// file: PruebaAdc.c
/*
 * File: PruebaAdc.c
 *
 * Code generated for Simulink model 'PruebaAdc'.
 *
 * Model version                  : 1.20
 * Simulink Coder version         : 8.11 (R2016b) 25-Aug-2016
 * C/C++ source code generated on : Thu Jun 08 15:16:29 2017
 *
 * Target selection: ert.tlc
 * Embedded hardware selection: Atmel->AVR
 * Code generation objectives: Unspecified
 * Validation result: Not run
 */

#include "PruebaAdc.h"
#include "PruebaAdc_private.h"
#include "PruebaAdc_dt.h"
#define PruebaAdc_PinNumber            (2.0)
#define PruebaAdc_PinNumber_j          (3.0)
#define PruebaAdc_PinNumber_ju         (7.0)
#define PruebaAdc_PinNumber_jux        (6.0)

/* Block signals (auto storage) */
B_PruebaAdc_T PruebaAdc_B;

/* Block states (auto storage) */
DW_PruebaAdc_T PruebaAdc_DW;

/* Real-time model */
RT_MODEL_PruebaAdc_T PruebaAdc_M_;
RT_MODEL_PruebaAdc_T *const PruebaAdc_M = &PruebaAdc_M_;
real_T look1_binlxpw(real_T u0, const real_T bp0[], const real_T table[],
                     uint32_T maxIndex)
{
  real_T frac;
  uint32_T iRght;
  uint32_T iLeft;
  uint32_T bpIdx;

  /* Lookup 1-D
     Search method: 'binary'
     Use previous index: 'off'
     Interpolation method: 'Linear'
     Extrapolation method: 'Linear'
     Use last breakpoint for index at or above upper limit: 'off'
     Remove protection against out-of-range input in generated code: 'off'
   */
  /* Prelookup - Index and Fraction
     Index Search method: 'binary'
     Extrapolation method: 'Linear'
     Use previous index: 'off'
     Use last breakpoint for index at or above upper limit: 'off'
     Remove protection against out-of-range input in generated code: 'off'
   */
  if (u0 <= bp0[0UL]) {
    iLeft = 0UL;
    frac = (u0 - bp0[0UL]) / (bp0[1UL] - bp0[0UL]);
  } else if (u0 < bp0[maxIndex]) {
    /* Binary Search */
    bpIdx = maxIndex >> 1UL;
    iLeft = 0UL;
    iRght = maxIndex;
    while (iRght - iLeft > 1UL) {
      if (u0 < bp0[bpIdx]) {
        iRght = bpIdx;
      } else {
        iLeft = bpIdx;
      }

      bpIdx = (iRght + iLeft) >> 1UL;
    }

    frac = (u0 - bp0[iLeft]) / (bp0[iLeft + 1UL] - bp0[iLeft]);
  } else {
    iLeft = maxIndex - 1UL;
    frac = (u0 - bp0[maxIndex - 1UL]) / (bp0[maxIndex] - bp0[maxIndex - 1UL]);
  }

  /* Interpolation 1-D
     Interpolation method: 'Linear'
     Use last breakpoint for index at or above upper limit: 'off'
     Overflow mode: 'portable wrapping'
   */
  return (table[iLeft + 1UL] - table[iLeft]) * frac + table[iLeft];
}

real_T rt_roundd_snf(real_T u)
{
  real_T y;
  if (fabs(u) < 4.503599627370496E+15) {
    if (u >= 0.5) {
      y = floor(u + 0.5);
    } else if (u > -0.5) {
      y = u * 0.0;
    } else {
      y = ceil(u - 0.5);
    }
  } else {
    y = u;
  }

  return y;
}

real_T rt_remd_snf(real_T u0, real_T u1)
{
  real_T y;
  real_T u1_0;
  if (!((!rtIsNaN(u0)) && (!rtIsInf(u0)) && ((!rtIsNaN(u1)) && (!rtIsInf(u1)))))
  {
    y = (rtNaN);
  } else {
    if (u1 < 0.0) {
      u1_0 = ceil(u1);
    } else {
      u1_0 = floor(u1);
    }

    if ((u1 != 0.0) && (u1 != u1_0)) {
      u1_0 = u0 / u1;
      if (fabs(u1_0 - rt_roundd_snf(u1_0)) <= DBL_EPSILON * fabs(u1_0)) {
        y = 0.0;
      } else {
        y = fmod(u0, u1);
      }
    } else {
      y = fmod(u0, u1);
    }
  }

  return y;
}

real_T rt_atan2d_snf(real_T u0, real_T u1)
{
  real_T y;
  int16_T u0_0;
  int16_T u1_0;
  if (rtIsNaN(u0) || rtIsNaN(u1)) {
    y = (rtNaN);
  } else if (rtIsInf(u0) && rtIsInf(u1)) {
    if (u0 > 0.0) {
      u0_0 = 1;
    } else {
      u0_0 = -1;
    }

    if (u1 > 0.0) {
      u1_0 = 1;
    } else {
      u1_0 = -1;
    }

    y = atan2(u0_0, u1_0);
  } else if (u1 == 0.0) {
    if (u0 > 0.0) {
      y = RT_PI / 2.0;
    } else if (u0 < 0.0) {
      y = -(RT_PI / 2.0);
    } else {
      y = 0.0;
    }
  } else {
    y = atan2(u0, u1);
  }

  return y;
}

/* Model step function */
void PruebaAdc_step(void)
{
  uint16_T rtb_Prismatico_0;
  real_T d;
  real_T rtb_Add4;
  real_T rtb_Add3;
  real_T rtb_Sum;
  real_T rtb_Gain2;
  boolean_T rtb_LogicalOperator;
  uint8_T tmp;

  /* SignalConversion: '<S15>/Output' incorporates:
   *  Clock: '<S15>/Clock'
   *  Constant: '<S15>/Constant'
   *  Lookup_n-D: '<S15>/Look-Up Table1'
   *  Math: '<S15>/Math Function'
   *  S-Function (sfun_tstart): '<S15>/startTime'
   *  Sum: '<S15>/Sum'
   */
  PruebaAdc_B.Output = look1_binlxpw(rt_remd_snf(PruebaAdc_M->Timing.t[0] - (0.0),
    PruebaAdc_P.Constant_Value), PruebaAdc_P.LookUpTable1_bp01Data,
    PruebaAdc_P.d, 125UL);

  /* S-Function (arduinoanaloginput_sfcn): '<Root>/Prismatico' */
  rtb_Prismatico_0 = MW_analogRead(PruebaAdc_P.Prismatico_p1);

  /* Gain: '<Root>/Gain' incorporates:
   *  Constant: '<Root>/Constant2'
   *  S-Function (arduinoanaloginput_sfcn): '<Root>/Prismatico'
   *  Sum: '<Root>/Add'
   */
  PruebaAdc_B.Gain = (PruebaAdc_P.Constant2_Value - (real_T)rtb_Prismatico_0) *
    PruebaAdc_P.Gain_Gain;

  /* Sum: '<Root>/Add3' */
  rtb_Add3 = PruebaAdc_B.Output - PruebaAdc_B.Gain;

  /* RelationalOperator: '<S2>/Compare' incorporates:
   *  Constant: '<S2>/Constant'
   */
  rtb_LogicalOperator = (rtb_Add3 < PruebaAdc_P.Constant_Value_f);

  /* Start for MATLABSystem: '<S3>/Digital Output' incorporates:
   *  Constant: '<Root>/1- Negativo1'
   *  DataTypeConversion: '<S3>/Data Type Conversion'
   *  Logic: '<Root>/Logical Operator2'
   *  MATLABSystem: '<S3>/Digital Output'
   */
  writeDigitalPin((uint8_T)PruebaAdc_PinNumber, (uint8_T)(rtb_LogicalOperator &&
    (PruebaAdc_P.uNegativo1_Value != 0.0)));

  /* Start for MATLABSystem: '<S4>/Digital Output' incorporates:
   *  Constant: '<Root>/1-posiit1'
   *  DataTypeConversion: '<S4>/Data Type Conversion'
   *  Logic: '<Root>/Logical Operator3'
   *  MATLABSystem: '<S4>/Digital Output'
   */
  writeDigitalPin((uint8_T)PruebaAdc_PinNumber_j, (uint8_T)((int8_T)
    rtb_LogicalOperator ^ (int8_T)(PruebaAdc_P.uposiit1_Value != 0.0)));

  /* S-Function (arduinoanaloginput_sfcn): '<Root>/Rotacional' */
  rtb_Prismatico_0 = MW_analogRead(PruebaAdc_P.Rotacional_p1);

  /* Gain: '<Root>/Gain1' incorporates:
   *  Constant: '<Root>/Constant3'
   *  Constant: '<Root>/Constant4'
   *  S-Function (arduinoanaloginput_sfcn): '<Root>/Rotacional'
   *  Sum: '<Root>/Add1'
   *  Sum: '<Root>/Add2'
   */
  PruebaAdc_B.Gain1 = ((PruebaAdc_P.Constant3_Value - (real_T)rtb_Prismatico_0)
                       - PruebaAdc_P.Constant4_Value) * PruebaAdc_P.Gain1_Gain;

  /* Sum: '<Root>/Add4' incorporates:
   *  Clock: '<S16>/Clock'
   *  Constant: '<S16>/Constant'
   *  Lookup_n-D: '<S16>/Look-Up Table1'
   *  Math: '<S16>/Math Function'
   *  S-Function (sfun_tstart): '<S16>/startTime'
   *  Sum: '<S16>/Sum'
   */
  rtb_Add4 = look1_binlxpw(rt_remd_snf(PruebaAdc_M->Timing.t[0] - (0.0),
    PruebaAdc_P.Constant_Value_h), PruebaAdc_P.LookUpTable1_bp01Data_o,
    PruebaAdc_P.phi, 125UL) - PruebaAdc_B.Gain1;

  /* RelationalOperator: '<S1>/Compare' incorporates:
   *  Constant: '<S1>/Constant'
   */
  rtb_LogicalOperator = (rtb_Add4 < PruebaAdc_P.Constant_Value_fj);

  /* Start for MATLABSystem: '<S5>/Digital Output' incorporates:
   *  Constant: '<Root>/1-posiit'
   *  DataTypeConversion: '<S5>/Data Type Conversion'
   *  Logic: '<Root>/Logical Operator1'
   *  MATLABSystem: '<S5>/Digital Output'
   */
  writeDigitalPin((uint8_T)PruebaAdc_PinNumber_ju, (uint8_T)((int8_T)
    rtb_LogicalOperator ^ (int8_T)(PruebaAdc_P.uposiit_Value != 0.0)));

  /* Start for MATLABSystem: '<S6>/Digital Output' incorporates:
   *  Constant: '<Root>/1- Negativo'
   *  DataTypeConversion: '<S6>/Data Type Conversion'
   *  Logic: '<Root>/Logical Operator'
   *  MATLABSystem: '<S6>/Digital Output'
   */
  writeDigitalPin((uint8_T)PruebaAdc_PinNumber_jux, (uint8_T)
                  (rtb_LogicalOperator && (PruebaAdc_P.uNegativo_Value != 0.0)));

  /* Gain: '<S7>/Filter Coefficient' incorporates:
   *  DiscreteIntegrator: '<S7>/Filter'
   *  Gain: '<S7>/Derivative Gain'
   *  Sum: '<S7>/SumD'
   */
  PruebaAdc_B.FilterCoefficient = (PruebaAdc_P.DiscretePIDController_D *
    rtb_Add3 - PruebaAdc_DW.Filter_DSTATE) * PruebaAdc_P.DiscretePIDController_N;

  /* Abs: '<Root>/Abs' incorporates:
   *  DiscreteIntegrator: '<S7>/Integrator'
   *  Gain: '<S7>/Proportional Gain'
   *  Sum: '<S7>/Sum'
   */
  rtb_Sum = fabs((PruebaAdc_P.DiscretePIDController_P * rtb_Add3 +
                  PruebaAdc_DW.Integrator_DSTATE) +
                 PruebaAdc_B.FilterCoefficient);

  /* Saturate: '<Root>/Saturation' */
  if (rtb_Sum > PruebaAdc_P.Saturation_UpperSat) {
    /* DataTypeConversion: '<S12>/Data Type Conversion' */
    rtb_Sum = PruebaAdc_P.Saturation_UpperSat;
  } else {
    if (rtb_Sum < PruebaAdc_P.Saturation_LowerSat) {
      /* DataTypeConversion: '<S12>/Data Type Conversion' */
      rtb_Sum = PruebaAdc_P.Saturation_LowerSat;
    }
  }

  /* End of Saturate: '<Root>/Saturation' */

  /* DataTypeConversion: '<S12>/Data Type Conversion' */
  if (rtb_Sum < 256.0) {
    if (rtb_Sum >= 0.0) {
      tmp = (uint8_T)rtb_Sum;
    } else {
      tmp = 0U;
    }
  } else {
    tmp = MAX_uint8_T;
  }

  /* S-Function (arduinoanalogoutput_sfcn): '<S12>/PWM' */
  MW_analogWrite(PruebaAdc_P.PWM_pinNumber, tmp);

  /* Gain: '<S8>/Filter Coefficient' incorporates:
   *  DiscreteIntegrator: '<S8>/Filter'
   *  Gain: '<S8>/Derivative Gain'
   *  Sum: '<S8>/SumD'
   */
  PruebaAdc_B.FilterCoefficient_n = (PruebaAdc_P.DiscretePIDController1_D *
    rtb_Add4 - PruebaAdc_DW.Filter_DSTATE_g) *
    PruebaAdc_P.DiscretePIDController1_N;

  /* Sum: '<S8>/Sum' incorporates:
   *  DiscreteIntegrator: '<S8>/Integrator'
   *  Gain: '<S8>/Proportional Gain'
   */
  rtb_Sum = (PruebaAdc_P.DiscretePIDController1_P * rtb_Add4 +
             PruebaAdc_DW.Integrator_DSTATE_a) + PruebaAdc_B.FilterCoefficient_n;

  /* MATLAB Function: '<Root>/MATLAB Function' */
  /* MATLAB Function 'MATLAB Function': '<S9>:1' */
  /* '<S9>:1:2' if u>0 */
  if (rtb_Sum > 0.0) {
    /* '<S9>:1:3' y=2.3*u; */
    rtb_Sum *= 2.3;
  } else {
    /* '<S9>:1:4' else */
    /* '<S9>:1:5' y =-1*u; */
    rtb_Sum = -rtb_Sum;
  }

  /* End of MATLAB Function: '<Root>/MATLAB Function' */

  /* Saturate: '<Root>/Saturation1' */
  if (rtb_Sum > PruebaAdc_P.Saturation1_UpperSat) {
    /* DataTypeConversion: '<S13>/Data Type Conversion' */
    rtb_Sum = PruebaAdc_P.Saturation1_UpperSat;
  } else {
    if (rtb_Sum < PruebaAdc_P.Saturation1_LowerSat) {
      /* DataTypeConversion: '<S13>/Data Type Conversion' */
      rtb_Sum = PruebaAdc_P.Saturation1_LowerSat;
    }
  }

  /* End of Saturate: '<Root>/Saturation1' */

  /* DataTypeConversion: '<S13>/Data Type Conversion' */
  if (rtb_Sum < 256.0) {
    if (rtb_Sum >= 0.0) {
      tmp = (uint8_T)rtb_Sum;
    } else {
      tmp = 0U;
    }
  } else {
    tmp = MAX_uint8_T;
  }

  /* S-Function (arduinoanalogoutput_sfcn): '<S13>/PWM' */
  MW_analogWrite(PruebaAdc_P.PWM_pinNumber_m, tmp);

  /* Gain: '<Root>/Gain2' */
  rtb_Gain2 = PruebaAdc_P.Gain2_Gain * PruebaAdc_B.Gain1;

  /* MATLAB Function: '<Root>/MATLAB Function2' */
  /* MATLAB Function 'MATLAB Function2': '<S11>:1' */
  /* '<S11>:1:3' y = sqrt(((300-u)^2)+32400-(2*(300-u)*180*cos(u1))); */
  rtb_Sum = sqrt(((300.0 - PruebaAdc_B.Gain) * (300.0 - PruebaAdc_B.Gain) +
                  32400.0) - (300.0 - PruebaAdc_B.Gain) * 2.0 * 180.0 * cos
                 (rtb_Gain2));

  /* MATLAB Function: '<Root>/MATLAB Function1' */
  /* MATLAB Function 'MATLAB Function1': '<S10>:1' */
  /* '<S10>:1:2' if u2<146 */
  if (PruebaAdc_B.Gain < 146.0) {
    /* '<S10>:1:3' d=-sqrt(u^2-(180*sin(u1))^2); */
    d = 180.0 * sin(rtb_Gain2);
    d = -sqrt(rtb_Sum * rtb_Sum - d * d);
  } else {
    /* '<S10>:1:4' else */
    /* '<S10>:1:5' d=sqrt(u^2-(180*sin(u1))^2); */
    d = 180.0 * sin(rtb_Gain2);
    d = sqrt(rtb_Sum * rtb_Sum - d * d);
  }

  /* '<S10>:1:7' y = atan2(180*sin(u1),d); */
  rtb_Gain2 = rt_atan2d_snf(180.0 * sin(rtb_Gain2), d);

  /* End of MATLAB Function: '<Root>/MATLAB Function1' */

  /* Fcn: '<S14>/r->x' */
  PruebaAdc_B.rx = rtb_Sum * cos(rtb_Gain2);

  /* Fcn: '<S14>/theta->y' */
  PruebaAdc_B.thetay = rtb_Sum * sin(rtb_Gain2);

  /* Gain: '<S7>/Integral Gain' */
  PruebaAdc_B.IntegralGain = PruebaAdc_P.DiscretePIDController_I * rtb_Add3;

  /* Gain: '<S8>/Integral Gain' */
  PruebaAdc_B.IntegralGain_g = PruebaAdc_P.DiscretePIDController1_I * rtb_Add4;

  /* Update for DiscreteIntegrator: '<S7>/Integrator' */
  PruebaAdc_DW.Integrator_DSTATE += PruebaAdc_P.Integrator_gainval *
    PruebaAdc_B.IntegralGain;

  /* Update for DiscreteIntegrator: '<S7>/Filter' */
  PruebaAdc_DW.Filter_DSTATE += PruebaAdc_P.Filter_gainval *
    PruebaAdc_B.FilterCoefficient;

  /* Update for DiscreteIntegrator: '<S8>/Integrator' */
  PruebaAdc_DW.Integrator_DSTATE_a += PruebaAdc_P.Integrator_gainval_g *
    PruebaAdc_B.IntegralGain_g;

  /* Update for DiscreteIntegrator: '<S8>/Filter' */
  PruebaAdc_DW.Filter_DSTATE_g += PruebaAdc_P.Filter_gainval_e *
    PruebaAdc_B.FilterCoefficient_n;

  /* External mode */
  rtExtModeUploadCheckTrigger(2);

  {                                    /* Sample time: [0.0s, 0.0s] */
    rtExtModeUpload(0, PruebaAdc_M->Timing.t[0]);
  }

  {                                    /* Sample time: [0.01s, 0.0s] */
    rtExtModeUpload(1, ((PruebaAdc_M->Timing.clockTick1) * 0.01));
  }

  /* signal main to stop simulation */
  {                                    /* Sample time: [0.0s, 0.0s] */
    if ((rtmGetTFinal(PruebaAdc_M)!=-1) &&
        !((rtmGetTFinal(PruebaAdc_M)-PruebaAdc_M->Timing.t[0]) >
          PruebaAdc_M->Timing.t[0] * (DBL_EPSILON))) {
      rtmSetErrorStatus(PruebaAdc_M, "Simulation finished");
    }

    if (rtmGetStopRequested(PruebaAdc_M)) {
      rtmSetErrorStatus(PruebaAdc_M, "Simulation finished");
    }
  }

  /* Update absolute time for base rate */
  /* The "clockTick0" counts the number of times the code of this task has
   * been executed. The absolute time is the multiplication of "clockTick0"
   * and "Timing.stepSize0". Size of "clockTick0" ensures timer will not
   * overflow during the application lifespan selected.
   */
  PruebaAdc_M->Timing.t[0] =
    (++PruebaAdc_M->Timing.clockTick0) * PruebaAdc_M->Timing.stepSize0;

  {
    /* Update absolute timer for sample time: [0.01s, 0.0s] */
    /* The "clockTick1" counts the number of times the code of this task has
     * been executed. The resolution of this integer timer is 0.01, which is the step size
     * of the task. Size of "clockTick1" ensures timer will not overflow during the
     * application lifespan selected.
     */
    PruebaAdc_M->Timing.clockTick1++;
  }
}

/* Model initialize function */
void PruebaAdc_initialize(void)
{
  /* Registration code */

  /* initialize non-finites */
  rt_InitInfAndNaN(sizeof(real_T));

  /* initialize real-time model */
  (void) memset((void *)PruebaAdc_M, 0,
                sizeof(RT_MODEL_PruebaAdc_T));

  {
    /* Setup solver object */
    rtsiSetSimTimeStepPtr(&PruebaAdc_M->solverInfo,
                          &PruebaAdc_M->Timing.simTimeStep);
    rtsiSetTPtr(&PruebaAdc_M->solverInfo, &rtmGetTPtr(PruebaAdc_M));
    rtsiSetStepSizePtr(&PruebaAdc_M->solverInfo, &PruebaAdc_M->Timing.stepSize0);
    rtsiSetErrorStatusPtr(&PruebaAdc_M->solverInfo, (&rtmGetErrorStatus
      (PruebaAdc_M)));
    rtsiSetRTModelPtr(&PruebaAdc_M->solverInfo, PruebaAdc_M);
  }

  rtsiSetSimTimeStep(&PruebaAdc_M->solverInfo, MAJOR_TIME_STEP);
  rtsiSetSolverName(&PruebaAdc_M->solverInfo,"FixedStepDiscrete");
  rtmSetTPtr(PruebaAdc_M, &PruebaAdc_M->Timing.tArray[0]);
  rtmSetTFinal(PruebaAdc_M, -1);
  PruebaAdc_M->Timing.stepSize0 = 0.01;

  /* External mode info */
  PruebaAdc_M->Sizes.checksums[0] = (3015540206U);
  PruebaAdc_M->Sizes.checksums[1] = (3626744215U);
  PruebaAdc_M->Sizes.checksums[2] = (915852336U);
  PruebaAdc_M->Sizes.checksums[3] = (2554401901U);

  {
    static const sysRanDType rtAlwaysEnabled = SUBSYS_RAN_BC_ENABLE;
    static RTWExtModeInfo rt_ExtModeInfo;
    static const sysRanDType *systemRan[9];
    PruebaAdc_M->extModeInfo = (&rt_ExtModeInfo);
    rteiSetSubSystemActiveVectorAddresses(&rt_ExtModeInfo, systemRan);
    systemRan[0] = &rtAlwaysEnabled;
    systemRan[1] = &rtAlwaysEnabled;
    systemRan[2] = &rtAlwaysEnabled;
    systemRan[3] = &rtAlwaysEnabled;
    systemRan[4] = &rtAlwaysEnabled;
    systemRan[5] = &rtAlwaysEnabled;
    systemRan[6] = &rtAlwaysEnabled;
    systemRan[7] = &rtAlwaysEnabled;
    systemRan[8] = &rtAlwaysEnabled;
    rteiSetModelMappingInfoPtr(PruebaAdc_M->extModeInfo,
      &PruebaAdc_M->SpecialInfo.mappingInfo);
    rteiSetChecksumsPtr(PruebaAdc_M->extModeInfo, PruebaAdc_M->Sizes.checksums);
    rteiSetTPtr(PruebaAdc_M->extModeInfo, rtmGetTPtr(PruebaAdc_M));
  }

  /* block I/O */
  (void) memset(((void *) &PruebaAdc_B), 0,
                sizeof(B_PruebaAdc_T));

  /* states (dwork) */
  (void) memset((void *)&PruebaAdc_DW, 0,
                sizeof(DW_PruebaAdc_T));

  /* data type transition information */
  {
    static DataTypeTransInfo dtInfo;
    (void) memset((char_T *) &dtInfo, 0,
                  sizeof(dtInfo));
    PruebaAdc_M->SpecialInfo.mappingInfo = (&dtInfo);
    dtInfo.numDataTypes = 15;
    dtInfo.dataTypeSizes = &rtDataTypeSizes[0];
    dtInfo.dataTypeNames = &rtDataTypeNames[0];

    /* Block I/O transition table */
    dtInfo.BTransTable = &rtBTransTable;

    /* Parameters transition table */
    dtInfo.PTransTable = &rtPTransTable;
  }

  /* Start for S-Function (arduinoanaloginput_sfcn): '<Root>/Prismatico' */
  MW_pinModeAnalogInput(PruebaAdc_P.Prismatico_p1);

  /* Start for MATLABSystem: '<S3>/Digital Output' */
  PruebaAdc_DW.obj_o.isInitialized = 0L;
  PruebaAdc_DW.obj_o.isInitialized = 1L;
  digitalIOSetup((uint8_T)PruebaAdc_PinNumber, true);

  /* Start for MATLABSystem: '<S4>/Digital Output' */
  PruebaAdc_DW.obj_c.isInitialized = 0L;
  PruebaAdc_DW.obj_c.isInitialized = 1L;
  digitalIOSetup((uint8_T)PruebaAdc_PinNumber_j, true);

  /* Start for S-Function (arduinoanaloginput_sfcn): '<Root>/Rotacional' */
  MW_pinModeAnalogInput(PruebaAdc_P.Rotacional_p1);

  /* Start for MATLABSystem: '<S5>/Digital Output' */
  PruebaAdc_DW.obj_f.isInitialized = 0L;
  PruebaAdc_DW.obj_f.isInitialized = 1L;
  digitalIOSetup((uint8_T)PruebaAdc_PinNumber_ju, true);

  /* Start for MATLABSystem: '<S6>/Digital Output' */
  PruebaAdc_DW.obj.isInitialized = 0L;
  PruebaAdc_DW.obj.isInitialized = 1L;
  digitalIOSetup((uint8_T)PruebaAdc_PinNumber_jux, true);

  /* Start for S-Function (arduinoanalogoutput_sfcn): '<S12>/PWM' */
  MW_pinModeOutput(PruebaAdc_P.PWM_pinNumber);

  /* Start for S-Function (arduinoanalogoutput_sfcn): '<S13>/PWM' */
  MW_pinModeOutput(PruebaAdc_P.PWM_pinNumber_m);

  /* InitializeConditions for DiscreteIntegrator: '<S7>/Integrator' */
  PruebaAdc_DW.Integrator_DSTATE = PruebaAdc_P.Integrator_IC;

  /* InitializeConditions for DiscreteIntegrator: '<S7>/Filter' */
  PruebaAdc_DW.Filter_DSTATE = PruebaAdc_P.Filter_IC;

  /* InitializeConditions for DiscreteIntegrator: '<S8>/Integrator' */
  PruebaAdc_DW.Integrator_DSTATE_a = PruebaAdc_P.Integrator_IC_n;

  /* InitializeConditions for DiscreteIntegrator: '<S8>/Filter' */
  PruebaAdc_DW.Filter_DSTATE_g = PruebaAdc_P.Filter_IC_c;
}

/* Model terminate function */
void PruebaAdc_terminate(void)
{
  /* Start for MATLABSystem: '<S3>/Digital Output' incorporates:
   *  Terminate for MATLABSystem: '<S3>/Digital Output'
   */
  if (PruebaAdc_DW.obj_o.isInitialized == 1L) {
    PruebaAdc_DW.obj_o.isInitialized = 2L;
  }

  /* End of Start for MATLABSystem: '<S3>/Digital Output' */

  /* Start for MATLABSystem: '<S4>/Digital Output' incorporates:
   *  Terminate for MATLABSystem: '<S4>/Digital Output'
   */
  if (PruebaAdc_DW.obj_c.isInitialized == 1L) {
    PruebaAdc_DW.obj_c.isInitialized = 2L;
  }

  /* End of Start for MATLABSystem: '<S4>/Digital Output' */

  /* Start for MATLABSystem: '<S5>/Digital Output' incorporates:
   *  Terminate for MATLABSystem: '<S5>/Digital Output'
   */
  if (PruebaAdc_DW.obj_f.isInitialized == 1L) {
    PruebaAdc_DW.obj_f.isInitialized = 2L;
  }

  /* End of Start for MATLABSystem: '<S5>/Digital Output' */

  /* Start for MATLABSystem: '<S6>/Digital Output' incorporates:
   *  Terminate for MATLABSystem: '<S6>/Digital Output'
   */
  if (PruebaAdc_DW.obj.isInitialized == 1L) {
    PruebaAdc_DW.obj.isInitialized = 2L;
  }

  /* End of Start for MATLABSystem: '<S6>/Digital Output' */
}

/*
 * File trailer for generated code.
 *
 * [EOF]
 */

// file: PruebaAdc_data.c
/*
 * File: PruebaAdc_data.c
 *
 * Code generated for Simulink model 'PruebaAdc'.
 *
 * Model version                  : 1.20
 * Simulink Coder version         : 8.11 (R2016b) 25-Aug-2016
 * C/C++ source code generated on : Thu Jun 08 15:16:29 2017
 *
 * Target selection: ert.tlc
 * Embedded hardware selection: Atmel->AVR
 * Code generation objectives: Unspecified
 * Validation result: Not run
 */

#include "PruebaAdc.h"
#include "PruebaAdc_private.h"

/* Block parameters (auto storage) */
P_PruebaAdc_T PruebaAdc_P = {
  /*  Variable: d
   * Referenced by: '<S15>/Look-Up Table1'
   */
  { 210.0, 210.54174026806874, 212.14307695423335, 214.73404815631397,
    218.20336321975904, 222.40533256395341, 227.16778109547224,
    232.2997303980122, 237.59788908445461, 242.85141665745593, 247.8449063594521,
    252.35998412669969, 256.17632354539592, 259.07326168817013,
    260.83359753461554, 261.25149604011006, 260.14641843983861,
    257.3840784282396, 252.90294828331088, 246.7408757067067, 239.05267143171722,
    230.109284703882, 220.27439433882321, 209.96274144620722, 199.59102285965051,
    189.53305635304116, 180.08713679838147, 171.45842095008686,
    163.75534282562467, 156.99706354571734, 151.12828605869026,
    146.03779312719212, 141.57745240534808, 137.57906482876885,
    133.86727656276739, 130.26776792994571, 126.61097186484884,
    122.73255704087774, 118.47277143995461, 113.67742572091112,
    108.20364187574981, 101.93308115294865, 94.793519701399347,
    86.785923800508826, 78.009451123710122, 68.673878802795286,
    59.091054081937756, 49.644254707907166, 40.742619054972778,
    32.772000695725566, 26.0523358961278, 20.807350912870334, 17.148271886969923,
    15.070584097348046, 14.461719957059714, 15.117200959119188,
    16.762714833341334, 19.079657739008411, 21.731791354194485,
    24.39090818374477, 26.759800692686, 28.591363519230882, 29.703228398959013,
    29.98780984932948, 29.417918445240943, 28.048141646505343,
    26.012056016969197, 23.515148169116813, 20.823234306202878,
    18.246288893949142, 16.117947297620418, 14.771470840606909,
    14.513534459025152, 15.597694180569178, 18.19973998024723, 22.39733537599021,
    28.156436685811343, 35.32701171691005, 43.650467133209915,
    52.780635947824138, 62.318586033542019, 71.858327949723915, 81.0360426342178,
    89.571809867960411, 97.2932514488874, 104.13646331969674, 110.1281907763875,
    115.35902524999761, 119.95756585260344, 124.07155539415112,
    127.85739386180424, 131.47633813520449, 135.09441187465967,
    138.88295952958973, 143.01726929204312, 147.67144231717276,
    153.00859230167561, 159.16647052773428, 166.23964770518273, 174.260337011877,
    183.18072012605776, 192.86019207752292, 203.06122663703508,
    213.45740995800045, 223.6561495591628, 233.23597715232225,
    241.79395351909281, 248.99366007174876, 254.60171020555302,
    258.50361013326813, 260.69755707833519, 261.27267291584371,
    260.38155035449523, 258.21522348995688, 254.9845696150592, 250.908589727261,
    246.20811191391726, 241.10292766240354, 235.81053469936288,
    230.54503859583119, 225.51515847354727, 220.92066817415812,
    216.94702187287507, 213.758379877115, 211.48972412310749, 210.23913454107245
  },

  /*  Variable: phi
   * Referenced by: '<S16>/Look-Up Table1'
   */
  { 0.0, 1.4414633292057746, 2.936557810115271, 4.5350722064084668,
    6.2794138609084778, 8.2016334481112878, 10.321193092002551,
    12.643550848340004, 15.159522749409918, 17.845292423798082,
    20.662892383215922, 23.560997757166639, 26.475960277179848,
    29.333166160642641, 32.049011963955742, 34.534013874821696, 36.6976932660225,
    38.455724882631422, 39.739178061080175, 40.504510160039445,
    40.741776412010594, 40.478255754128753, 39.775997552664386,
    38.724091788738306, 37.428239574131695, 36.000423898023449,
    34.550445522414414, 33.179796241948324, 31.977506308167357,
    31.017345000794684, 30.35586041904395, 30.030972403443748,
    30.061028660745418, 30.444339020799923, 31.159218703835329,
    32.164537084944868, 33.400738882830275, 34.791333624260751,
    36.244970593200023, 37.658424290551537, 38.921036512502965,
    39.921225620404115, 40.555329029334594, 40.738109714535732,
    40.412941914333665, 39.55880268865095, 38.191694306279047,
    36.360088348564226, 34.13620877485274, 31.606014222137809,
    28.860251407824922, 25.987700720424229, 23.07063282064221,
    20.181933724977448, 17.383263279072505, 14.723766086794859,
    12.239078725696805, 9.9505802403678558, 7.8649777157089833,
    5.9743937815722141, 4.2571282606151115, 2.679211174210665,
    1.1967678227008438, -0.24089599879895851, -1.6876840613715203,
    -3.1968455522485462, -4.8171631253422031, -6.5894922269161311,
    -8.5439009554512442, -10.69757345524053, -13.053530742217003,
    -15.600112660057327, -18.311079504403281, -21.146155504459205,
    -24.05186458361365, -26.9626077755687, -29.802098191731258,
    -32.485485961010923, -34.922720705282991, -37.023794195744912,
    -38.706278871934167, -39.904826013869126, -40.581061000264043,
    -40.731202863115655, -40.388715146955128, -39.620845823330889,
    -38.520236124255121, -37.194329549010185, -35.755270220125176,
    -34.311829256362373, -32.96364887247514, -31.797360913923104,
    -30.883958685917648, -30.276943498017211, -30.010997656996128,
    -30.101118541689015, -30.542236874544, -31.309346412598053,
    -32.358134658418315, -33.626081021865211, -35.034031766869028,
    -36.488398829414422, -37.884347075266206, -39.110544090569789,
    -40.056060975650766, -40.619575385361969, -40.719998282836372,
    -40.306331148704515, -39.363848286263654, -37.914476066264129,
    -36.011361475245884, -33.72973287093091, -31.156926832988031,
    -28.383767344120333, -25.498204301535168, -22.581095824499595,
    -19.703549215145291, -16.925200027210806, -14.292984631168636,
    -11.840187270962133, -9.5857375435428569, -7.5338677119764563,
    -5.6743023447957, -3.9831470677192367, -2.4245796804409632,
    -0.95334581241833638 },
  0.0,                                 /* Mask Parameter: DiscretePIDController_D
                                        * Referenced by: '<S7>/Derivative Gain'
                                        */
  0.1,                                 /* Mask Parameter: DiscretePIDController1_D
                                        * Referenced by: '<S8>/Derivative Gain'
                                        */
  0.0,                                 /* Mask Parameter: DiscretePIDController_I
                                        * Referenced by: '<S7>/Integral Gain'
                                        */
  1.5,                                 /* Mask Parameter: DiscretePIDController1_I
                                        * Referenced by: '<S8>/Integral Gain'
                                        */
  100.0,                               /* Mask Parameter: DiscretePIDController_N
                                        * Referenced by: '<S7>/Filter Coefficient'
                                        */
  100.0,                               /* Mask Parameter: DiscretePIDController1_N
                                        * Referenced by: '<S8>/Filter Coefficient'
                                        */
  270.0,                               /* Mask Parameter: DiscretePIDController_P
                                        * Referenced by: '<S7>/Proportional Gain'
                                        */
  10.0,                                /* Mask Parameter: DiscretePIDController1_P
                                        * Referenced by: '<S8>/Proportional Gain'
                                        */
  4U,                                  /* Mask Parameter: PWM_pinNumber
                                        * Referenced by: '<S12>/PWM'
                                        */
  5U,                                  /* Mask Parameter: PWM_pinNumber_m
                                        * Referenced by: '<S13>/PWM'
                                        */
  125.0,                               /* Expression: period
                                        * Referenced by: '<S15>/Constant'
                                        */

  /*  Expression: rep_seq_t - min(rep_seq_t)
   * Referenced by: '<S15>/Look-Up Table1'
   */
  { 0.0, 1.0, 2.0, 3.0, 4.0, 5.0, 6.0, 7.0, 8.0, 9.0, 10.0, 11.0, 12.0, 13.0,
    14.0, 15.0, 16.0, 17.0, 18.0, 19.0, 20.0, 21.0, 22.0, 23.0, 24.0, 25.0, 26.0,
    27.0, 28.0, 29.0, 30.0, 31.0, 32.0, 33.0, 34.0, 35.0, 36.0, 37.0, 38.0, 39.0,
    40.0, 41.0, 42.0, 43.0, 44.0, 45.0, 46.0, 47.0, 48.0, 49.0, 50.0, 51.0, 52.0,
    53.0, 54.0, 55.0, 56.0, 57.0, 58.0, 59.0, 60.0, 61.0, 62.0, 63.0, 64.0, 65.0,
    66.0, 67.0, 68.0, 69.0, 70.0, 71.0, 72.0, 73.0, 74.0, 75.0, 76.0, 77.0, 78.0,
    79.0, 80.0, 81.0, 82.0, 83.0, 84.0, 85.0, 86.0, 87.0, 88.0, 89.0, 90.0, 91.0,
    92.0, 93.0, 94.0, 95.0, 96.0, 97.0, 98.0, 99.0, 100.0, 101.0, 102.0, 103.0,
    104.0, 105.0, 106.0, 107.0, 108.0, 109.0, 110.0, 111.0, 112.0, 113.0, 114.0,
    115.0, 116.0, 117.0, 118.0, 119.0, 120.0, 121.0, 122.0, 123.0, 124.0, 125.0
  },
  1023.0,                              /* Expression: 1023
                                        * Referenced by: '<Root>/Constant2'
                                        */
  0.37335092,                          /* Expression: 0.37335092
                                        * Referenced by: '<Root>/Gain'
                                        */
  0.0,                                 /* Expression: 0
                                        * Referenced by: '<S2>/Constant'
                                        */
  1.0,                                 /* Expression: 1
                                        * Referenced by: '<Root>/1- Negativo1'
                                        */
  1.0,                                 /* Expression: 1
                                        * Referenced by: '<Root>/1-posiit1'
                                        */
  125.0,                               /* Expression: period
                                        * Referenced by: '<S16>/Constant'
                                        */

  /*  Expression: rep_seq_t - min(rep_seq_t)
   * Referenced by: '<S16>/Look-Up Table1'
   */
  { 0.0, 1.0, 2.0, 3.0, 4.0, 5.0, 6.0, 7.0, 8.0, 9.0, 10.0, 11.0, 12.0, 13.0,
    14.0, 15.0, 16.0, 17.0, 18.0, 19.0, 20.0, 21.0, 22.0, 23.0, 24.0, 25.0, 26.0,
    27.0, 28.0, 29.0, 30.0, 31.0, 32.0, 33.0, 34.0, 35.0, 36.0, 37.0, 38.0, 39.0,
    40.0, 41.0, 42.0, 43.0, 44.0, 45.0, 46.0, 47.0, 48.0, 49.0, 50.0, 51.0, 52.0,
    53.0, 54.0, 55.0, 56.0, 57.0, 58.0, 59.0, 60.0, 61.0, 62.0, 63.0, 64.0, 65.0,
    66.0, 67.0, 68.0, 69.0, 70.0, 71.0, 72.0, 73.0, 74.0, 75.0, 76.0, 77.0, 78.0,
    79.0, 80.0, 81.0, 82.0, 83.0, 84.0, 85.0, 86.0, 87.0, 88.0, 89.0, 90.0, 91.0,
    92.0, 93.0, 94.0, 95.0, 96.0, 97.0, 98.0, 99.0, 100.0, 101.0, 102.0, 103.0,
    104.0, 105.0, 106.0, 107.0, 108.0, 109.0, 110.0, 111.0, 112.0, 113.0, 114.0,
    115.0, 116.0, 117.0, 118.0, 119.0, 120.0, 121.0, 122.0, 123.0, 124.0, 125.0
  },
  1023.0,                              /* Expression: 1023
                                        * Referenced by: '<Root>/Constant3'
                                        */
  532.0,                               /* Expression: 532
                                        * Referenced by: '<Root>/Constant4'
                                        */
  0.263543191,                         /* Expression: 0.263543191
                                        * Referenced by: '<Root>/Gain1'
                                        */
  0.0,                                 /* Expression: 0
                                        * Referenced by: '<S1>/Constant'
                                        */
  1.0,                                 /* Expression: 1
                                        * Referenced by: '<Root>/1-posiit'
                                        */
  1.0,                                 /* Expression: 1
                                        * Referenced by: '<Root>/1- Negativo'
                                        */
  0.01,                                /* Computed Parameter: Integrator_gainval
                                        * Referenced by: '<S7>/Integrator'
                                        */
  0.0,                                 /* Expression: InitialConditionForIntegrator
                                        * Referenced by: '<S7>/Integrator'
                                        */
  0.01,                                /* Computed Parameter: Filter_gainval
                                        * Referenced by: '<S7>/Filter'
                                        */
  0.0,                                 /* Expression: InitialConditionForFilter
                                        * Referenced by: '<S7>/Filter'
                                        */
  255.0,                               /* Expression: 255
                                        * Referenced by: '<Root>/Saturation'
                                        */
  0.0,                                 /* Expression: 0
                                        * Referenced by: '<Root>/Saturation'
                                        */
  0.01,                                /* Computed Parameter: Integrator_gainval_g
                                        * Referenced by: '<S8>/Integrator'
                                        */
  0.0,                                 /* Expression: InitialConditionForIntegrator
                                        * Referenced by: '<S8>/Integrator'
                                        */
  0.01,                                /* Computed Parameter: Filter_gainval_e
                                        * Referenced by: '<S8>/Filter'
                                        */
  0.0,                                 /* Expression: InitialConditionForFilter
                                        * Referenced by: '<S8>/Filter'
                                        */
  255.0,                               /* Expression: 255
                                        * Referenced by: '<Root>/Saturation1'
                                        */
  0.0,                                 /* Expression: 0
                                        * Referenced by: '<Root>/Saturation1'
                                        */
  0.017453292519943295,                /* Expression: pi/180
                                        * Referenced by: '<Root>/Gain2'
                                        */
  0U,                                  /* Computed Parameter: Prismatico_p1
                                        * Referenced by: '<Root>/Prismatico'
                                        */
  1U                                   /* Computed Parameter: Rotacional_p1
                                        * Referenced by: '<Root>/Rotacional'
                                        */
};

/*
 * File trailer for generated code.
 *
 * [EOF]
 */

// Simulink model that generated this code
simulink model "PruebaAdc"  (R2016b)
settings: Solver=FixedStepDiscrete  StartTime=0.0  StopTime=inf  FixedStep=0.01  RelTol=1e-3  EnableMultiTasking=on
libraries: arduinolib x8, simulink x7, simulink_extras x1

== system PruebaAdc ==
  1- Negativo : Constant
  1- Negativo1 : Constant
  1-posiit : Constant
  1-posiit1 : Constant
  Abs : Abs
  Add{,1..4} (5 alike) : Sum  Inputs=+-
  Compare To Zero : simulink/Logic and Bit Operations/Compare To Zero  relop=<  OutDataTypeStr=boolean
  Compare To Zero1 : simulink/Logic and Bit Operations/Compare To Zero  relop=<  OutDataTypeStr=boolean
  Constant2 : Constant  Value=1023
  Constant3 : Constant  Value=1023
  Constant4 : Constant  Value=532
  Digital Output : arduinolib/Digital Output  pinNumber=2  blockPlatform=arduino
  Digital Output1 : arduinolib/Digital Output  pinNumber=3  blockPlatform=arduino
  Digital Output2 : arduinolib/Digital Output  pinNumber=7  blockPlatform=arduino
  Digital Output3 : arduinolib/Digital Output  pinNumber=6  blockPlatform=arduino
  Discrete PID Controller : simulink/Continuous/PID Controller  Controller=PID  TimeDomain=Discrete-time  SampleTime=-1  IntegratorMethod=Forward Euler  FilterMethod=Forward Euler  Form=Parallel  UseFilter=on  ControllerParametersSource=internal  P=270  I=0  D=0  N=100  InitialConditionSource=internal  InitialConditionForIntegrator=0  InitialConditionForFilter=0  ExternalReset=none  LimitOutput=off  UpperSaturationLimit=inf  LowerSaturationLimit=-inf  LinearizeAsGain=off  AntiWindupMode=none  Kb=1  TrackingMode=off  Kt=1  PParamMin=[]  PParamMax=[]  IParamMin=[]  IParamMax=[]  DParamMin=[]  DParamMax=[]  NParamMin=[]  NParamMax=[]  KbParamMin=[]  KbParamMax=[]  KtParamMin=[]  KtParamMax=[]  POutMin=[]  POutMax=[]  IOutMin=[]  IOutMax=[]  DOutMin=[]  DOutMax=[]  NOutMin=[]  NOutMax=[]  KbOutMin=[]  KbOutMax=[]  KtOutMin=[]  KtOutMax=[]  IntegratorOutMin=[]  IntegratorOutMax=[]  FilterOutMin=[]  FilterOutMax=[]  SumOutMin=[]  SumOutMax=[]  SumI1OutMin=[]  SumI1OutMax=[]  SumI2OutMin=[]  SumI2OutMax=[]  SumI3OutMin=[]  SumI3OutMax=[]  SumDOutMin=[]  SumDOutMax=[]  SaturationOutMin=[]  SaturationOutMax=[]  IntegratorContinuousStateAttributes=''  IntegratorStateMustResolveToSignalObject=off  IntegratorRTWStateStorageClass=Auto  FilterContinuousStateAttributes=''  FilterStateMustResolveToSignalObject=off  FilterRTWStateStorageClass=Auto  DifferentiatorICPrevScaledInput=0  DifferentiatorOutMin=[]  DifferentiatorOutMax=[]
  Discrete PID Controller1 : simulink/Continuous/PID Controller  Controller=PID  TimeDomain=Discrete-time  SampleTime=-1  IntegratorMethod=Forward Euler  FilterMethod=Forward Euler  Form=Parallel  UseFilter=on  ControllerParametersSource=internal  P=10  I=1.5  D=0.1  N=100  InitialConditionSource=internal  InitialConditionForIntegrator=0  InitialConditionForFilter=0  ExternalReset=none  LimitOutput=off  UpperSaturationLimit=inf  LowerSaturationLimit=-inf  LinearizeAsGain=off  AntiWindupMode=none  Kb=1  TrackingMode=off  Kt=1  PParamMin=[]  PParamMax=[]  IParamMin=[]  IParamMax=[]  DParamMin=[]  DParamMax=[]  NParamMin=[]  NParamMax=[]  KbParamMin=[]  KbParamMax=[]  KtParamMin=[]  KtParamMax=[]  POutMin=[]  POutMax=[]  IOutMin=[]  IOutMax=[]  DOutMin=[]  DOutMax=[]  NOutMin=[]  NOutMax=[]  KbOutMin=[]  KbOutMax=[]  KtOutMin=[]  KtOutMax=[]  IntegratorOutMin=[]  IntegratorOutMax=[]  FilterOutMin=[]  FilterOutMax=[]  SumOutMin=[]  SumOutMax=[]  SumI1OutMin=[]  SumI1OutMax=[]  SumI2OutMin=[]  SumI2OutMax=[]  SumI3OutMin=[]  SumI3OutMax=[]  SumDOutMin=[]  SumDOutMax=[]  SaturationOutMin=[]  SaturationOutMax=[]  IntegratorContinuousStateAttributes=''  IntegratorStateMustResolveToSignalObject=off  IntegratorRTWStateStorageClass=Auto  FilterContinuousStateAttributes=''  FilterStateMustResolveToSignalObject=off  FilterRTWStateStorageClass=Auto  DifferentiatorICPrevScaledInput=0  DifferentiatorOutMin=[]  DifferentiatorOutMax=[]
  Gain : Gain  Gain=0.37335092
  Gain1 : Gain  Gain=0.263543191
  Gain2 : Gain  Gain=pi/180
  Logical Operator : Logic  AllPortsSameDT=off  OutDataTypeStr=boolean
  Logical Operator1 : Logic  Operator=XOR  AllPortsSameDT=off  OutDataTypeStr=boolean
  Logical Operator2 : Logic  AllPortsSameDT=off  OutDataTypeStr=boolean
  Logical Operator3 : Logic  Operator=XOR  AllPortsSameDT=off  OutDataTypeStr=boolean
  MATLAB Function : MATLAB Function  TreatAsAtomicUnit=on
  MATLAB Function1 : MATLAB Function  TreatAsAtomicUnit=on
  MATLAB Function2 : MATLAB Function  TreatAsAtomicUnit=on
  Mux : Mux  Inputs=2
  PWM : arduinolib/PWM  pinNumber=4  blockPlatform=arduino
  PWM1 : arduinolib/PWM  pinNumber=5  blockPlatform=arduino
  Polar to Cartesian : simulink_extras/Transformations/Polar to Cartesian
  Posicion grados : Scope
  Posicion mm : Scope
  Prismatico : arduinolib/Analog Input  pinNumber=0  sampleTime=0.01  blockPlatform=arduino
  Repeating Sequence : simulink/Sources/Repeating Sequence  rep_seq_t=t  rep_seq_y=d
  Repeating Sequence1 : simulink/Sources/Repeating Sequence  rep_seq_t=t  rep_seq_y=phi
  Rotacional : arduinolib/Analog Input  pinNumber=1  sampleTime=0.01  blockPlatform=arduino
  Saturation : Saturate  UpperLimit=255  LowerLimit=0
  Saturation1 : Saturate  UpperLimit=255  LowerLimit=0
  XY Graph : simulink/Sinks/XY Graph  xmin=-200  xmax=200  ymin=-200  ymax=200  st=-1
  wires:
  Prismatico/1 -> Add/2
  Constant2/1 -> Add/1
  Add/1 -> Gain/1
  Gain/1 -> MATLAB Function1/3(u2), MATLAB Function2/1(u), Mux/1, Add3/2
  Discrete PID Controller/1 -> Abs/1
  Rotacional/1 -> Add1/2
  Constant3/1 -> Add1/1
  Add2/1 -> Gain1/1
  Add1/1 -> Add2/1
  Constant4/1 -> Add2/2
  Repeating Sequence1/1 -> Add4/1
  Add4/1 -> Discrete PID Controller1/1, Compare To Zero/1
  1-posiit/1 -> Logical Operator1/2
  Compare To Zero/1 -> Logical Operator1/1, Logical Operator/1
  Logical Operator1/1 -> Digital Output2/1
  1- Negativo/1 -> Logical Operator/2
  Logical Operator/1 -> Digital Output3/1
  Discrete PID Controller1/1 -> MATLAB Function/1(u)
  Add3/1 -> Compare To Zero1/1, Discrete PID Controller/1
  1-posiit1/1 -> Logical Operator3/2
  Compare To Zero1/1 -> Logical Operator3/1, Logical Operator2/1
  Logical Operator3/1 -> Digital Output1/1
  1- Negativo1/1 -> Logical Operator2/2
  Logical Operator2/1 -> Digital Output/1
  Repeating Sequence/1 -> Mux/2, Add3/1
  Saturation/1 -> PWM/1
  Abs/1 -> Saturation/1
  MATLAB Function/1(y) -> Saturation1/1
  Saturation1/1 -> PWM1/1
  Mux/1 -> Posicion mm/1
  Gain1/1 -> Gain2/1, Posicion grados/1, Add4/2
  Gain2/1 -> MATLAB Function1/2(u1), MATLAB Function2/2(u1)
  MATLAB Function2/1(y) -> Polar to Cartesian/1, MATLAB Function1/1(u)
  MATLAB Function1/1(y) -> Polar to Cartesian/2
  Polar to Cartesian/1 -> XY Graph/1
  Polar to Cartesian/2 -> XY Graph/2

== matlab function PruebaAdc/MATLAB Function1 ==
function y = fcn(u,u1,u2)
if u2<146
d=-sqrt(u^2-(180*sin(u1))^2);
else
d=sqrt(u^2-(180*sin(u1))^2);
end
y = atan2(180*sin(u1),d);

== matlab function PruebaAdc/MATLAB Function ==
function y = fcn(u)
if u>0
    y=2.3*u;
else
    y =-1*u;
end
end

== matlab function PruebaAdc/MATLAB Function2 ==
function y = fcn(u,u1)

y = sqrt(((300-u)^2)+32400-(2*(300-u)*180*cos(u1)));
